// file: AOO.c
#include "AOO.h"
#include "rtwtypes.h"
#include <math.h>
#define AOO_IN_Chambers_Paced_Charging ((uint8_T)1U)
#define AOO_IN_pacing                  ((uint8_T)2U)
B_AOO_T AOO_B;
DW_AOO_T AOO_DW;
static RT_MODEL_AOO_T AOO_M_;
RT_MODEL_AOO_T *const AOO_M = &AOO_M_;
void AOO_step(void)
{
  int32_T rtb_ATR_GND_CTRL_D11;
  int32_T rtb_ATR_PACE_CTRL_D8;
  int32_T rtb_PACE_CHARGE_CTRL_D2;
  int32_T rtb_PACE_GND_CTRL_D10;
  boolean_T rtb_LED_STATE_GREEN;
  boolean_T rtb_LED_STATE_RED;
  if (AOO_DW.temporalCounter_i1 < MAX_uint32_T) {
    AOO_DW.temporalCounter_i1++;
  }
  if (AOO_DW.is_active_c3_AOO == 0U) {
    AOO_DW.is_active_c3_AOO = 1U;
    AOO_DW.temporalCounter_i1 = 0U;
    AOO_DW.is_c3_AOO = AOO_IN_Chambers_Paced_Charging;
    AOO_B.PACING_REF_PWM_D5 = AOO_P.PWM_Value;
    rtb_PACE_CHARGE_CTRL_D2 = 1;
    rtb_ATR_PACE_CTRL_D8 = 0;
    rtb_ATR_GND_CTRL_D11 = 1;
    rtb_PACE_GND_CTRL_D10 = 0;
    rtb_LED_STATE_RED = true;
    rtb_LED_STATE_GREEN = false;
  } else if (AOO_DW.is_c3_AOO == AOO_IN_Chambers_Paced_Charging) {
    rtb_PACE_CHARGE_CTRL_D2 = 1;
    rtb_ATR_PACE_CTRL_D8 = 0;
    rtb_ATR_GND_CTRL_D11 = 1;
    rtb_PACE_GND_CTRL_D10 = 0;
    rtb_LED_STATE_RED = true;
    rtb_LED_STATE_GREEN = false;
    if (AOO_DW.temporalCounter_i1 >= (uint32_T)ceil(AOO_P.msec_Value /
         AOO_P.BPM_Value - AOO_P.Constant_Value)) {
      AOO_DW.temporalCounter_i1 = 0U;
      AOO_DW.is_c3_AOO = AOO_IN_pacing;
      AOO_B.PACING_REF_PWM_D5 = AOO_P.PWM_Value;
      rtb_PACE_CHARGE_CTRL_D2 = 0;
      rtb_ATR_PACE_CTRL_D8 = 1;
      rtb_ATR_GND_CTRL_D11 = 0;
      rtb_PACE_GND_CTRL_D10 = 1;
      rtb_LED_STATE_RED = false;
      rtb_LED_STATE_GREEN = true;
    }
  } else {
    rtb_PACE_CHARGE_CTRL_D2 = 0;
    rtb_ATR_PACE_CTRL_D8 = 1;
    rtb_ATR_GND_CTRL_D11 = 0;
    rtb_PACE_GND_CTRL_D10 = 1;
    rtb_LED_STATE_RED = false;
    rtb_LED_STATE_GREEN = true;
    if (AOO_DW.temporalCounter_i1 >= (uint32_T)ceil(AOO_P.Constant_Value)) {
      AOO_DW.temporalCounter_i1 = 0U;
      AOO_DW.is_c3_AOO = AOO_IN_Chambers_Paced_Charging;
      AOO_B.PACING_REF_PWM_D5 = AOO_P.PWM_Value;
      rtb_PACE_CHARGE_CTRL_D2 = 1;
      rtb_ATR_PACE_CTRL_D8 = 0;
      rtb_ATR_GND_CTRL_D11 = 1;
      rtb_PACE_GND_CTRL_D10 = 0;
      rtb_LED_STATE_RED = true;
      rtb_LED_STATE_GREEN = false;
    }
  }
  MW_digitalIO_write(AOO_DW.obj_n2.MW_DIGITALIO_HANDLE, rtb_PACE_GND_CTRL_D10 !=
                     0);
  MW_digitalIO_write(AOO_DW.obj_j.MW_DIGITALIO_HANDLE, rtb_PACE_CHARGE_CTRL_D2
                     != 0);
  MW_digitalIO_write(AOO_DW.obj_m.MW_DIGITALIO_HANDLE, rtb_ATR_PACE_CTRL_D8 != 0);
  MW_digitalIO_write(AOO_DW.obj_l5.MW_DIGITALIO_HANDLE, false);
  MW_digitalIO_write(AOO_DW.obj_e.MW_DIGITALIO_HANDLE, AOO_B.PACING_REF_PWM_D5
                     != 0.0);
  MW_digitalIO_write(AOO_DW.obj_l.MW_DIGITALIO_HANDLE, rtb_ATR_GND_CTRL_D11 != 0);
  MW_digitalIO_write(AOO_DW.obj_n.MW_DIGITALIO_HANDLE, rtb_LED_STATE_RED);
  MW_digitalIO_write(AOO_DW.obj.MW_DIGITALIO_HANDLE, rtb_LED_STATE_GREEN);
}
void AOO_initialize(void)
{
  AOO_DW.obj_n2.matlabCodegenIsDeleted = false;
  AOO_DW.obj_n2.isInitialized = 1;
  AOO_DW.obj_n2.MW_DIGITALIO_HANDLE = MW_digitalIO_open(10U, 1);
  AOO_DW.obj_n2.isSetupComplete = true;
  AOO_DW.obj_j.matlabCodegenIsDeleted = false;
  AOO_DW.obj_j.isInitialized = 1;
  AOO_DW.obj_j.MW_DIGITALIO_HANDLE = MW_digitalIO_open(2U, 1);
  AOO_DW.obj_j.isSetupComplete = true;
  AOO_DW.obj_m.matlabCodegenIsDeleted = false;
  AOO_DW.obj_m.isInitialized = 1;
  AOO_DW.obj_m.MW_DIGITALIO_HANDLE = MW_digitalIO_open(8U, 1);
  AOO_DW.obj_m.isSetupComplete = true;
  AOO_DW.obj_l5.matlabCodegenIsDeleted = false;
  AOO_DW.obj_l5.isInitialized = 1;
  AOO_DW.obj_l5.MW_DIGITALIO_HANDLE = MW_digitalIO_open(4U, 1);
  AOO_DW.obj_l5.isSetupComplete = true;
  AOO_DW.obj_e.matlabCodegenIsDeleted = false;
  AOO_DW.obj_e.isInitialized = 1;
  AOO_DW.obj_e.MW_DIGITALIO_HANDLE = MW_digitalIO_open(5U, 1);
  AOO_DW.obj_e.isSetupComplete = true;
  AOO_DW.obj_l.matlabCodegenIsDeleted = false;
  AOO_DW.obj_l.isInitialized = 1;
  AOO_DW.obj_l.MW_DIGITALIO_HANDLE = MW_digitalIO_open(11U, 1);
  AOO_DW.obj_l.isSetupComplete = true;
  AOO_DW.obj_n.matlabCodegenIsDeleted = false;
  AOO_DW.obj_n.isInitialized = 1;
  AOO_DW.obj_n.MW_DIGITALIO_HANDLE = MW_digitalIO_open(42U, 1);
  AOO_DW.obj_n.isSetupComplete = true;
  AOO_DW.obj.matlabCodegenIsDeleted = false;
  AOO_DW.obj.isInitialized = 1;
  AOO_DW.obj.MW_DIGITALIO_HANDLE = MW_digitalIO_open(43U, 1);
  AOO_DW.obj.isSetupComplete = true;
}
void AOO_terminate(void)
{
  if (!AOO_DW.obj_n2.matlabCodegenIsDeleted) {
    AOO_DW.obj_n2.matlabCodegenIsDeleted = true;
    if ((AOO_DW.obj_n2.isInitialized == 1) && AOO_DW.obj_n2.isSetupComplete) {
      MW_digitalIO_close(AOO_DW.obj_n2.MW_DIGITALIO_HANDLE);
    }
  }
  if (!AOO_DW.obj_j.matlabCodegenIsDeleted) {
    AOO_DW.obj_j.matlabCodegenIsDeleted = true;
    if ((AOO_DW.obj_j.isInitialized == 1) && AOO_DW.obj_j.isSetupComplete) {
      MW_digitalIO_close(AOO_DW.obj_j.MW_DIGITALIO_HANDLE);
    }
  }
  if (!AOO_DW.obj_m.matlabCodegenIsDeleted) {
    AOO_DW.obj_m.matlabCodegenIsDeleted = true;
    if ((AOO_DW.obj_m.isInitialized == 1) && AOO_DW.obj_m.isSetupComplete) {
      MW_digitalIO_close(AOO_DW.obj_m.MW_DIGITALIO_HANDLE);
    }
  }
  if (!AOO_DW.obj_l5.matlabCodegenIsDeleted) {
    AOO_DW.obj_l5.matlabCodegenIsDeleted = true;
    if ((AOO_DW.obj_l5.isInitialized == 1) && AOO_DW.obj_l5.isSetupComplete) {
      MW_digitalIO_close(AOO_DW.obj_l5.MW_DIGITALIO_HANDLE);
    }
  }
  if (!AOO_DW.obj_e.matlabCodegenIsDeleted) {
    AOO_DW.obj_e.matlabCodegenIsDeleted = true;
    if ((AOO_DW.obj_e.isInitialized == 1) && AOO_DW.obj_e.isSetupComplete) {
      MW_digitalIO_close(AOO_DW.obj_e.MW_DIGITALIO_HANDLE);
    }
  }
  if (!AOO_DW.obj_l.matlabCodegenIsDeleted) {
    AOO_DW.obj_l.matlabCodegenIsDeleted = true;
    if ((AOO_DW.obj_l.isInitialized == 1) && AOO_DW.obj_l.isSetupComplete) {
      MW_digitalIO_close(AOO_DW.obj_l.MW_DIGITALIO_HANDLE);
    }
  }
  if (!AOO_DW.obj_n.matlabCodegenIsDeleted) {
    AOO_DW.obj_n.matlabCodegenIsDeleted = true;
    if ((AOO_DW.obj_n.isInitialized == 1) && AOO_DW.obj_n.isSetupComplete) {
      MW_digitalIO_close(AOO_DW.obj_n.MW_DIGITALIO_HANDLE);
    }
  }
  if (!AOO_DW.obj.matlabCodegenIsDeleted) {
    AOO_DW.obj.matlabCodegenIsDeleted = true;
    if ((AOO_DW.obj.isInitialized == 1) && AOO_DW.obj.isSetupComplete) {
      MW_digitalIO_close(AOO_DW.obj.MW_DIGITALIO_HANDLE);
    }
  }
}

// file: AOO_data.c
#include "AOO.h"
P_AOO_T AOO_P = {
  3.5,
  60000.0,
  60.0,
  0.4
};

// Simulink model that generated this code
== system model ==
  DigitalWrite#1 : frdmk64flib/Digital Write  <- 1: AOO/2
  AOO : Stateflow chart  <- 1: PWM, 2: Product#1, 3: Constant
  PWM : Constant  Value=3.5
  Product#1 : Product  Inputs=*/  <- 1: msec, 2: BPM
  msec : Constant  Value=60000
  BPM : Constant  Value=60
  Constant : Constant  Value=0.4
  DigitalWrite#2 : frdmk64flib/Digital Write  <- 1: AOO
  DigitalWrite#3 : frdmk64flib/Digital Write  <- 1: AOO/3
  DigitalWrite#4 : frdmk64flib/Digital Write  <- 1: AOO/5
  DigitalWrite#5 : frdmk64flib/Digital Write  <- 1: AOO/6
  DigitalWrite#6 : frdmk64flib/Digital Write  <- 1: AOO/4
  DigitalWrite#7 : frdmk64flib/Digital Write  <- 1: AOO/7
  DigitalWrite#8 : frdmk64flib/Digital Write  <- 1: AOO/8
== stateflow chart AOO ==
  state pacing
    entry:
    PACING_REF_PWM_D5 = Amp;
    PACE_CHARGE_CTRL_D2=0;
    ATR_PACE_CTRL_D8= 1;
    ATR_GND_CTRL_D11= 0;
    PACE_GND_CTRL_D10=1;
    Z_ATR_CTRL_D4=0;
    LED_STATE_RED=false;
    LED_STATE_GREEN=true;
  state Chambers_Paced_Charging
    entry:
    PACING_REF_PWM_D5 = Amp;
    PACE_CHARGE_CTRL_D2=1;
    ATR_PACE_CTRL_D8= 0;
    ATR_GND_CTRL_D11= 1;
    PACE_GND_CTRL_D10=0;
    Z_ATR_CTRL_D4=0;
    LED_STATE_RED=true;
    LED_STATE_GREEN=false;
  (default) -> Chambers_Paced_Charging
  Chambers_Paced_Charging -> pacing : [after(Pulse_Period-Pulse_Width,msec)]
  pacing -> Chambers_Paced_Charging : [after(Pulse_Width,msec)]
  data: PACE_CHARGE_CTRL_D2 output; PACE_GND_CTRL_D10 output; ATR_PACE_CTRL_D8 output; ATR_GND_CTRL_D11 output; Z_ATR_CTRL_D4 output; PACING_REF_PWM_D5 output; Amp input; LED_STATE_RED output; LED_STATE_GREEN output; Pulse_Period input; Pulse_Width input
